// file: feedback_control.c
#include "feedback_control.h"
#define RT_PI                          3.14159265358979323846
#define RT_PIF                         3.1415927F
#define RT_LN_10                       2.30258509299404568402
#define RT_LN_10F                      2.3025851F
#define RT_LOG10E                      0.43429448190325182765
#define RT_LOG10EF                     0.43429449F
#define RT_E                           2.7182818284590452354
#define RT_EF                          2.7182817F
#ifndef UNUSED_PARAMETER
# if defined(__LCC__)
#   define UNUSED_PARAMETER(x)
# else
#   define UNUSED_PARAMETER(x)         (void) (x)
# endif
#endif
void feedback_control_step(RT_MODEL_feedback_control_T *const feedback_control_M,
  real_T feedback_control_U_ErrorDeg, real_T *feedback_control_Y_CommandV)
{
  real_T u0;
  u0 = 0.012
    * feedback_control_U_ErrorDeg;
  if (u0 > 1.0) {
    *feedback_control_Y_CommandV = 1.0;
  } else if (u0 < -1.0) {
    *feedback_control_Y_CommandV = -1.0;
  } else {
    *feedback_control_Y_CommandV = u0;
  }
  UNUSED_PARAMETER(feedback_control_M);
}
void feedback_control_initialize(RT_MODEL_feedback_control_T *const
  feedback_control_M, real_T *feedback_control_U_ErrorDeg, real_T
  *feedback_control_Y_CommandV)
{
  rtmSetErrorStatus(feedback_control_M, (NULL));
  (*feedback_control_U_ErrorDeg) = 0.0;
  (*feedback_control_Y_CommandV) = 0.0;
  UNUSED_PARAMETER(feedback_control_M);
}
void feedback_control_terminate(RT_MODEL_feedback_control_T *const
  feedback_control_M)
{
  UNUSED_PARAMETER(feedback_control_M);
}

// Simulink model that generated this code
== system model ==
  ErrorDeg : Inport
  CommandV : Outport  <- 1: Saturate#1
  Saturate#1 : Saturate  UpperLimit=1  LowerLimit=-1  <- 1: Gain#1
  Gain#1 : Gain  Gain=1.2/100  <- 1: ErrorDeg
